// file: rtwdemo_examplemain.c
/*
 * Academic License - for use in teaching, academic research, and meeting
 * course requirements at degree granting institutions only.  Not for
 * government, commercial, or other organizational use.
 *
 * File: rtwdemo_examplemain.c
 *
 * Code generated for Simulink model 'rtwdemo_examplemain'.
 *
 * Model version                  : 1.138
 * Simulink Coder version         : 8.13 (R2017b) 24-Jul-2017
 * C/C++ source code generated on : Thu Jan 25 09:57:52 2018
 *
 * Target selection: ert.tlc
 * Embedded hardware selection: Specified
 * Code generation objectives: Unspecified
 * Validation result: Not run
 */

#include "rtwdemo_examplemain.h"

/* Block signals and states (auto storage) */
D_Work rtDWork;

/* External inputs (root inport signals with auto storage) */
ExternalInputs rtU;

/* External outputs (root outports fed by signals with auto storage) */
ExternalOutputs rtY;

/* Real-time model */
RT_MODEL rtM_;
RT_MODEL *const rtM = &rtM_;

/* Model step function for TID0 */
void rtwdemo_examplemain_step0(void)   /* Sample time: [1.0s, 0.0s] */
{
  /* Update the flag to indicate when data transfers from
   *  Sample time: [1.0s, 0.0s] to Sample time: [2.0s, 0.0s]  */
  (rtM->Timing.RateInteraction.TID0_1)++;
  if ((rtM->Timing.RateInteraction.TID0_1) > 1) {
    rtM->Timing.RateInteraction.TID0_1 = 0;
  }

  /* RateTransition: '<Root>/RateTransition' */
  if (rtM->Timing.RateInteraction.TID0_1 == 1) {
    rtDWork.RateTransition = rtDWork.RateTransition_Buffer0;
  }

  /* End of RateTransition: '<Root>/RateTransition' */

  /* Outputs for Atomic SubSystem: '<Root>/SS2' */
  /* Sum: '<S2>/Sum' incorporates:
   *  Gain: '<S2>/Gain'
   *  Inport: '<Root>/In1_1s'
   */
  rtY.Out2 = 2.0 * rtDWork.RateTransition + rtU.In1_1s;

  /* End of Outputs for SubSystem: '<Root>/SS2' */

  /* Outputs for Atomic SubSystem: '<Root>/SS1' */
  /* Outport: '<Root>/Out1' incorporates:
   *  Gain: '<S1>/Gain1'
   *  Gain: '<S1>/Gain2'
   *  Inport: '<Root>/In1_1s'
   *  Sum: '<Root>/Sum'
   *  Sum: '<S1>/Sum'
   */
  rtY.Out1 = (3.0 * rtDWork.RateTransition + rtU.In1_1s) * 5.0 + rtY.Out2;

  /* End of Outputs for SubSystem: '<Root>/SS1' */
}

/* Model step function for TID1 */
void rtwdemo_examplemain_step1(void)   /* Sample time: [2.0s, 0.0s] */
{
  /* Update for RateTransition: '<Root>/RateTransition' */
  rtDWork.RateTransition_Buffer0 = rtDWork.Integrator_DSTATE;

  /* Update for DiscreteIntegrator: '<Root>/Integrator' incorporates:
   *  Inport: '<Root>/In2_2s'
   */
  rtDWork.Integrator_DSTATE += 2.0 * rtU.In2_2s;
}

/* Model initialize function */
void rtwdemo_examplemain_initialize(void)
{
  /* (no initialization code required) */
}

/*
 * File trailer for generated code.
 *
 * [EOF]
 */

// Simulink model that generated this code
simulink model "rtwdemo_examplemain"  (R2017b)
settings: Solver=FixedStepDiscrete  StartTime=0.0  StopTime=10.0  FixedStep=1  RelTol=1e-3  EnableMultiTasking=on
undefined symbols (not defined in the file): DiscIntNeverNeededParam
libraries: rtwdemowidgets x2

== system rtwdemo_examplemain ==
  note: \bfDescription\rm
      | This model shows the "Generate an example main program" feature of Embedded Coder.
      | The model is configured to generate a main program suitable for deployment on a bare-board
      | target (one with no operating system).  Alternatively, you can configure the model to generate
      | an example main program for deployment on a VxWorks operating system target.
      | The example ert\_main.c that is generated for the model shows how to deploy the code.
      |
      | You can customize a generated main program using the Embedded Coder(R) "File customization
      | template," which is located on the Code Generation Templates page.
      | See the Embedded Coder documentation for a description of this feature.
      |
      | \bfInstructions\rm
      | To select the "Generate an example main program" option,
      | 1. From the menu bar, choose Simulation > Model Configuration Parameters.
      | 2. Select the Code Generation Templates page.
      | 3. Select "Generate an example main program."
      | 4. Configure "Target operating system."
  note: Copyright 1994-2012 The MathWorks, Inc.
  In1_1s : Inport  OutDataTypeStr=double  PortDimensions=1  SampleTime=1
  In2_2s : Inport  Port=2  OutDataTypeStr=double  PortDimensions=1  SampleTime=2
  Build ERT : rtwdemowidgets/Build ERT  attrib_overrides={'TargetOS'}
  Integrator : DiscreteIntegrator  InitialConditionSetting=State (most efficient)  SampleTime=-1  SaturateOnIntegerOverflow=on  ICPrevOutput=DiscIntNeverNeededParam  ICPrevScaledInput=DiscIntNeverNeededParam
  RateTransition : RateTransition
  SS1 : Subsystem  TreatAsAtomicUnit=on
  SS2 : Subsystem  TreatAsAtomicUnit=on
  Sum : Sum  Inputs=|++  SaturateOnIntegerOverflow=on  InputSameDT=on  OutDataTypeStr=Inherit: Same as first input
  View Code Generation Templates : rtwdemowidgets/View Code Generation Templates  SystemSampleTime=-1
  Out1 : Outport
  Out2 : Outport  Port=2
  wires:
  In1_1s/1 -> SS1/1(In1), SS2/2(In2)
  In2_2s/1 -> Integrator/1
  SS2/1(Out1) -> Out2/1, Sum/2
  SS1/1(Out1) -> Sum/1
  Sum/1 -> Out1/1
  RateTransition/1 -> SS2/1(In1), SS1/2(In2)
  Integrator/1 -> RateTransition/1

== system rtwdemo_examplemain/SS1 ==
  In1 : Inport
  In2 : Inport  Port=2
  Gain1 : Gain  Gain=3  SaturateOnIntegerOverflow=on  OutDataTypeStr=Inherit: Same as input  ParamDataTypeStr=Inherit: Same as input
  Gain2 : Gain  Gain=5  SaturateOnIntegerOverflow=on  OutDataTypeStr=Inherit: Same as input  ParamDataTypeStr=Inherit: Same as input
  Sum : Sum  Inputs=|++  SaturateOnIntegerOverflow=on  InputSameDT=on  OutDataTypeStr=Inherit: Same as first input
  Out1 : Outport
  wires:
  In1/1 -> Sum/1
  Sum/1 -> Gain2/1
  In2/1 -> Gain1/1
  Gain2/1 -> Out1/1
  Gain1/1 -> Sum/2

== system rtwdemo_examplemain/SS2 ==
  In1 : Inport
  In2 : Inport  Port=2
  Gain : Gain  Gain=2  SaturateOnIntegerOverflow=on  OutDataTypeStr=Inherit: Same as input  ParamDataTypeStr=Inherit: Same as input
  Sum : Sum  Inputs=|++  SaturateOnIntegerOverflow=on  InputSameDT=on  OutDataTypeStr=Inherit: Same as first input
  Out1 : Outport
  wires:
  In1/1 -> Gain/1
  Gain/1 -> Sum/1
  Sum/1 -> Out1/1
  In2/1 -> Sum/2
